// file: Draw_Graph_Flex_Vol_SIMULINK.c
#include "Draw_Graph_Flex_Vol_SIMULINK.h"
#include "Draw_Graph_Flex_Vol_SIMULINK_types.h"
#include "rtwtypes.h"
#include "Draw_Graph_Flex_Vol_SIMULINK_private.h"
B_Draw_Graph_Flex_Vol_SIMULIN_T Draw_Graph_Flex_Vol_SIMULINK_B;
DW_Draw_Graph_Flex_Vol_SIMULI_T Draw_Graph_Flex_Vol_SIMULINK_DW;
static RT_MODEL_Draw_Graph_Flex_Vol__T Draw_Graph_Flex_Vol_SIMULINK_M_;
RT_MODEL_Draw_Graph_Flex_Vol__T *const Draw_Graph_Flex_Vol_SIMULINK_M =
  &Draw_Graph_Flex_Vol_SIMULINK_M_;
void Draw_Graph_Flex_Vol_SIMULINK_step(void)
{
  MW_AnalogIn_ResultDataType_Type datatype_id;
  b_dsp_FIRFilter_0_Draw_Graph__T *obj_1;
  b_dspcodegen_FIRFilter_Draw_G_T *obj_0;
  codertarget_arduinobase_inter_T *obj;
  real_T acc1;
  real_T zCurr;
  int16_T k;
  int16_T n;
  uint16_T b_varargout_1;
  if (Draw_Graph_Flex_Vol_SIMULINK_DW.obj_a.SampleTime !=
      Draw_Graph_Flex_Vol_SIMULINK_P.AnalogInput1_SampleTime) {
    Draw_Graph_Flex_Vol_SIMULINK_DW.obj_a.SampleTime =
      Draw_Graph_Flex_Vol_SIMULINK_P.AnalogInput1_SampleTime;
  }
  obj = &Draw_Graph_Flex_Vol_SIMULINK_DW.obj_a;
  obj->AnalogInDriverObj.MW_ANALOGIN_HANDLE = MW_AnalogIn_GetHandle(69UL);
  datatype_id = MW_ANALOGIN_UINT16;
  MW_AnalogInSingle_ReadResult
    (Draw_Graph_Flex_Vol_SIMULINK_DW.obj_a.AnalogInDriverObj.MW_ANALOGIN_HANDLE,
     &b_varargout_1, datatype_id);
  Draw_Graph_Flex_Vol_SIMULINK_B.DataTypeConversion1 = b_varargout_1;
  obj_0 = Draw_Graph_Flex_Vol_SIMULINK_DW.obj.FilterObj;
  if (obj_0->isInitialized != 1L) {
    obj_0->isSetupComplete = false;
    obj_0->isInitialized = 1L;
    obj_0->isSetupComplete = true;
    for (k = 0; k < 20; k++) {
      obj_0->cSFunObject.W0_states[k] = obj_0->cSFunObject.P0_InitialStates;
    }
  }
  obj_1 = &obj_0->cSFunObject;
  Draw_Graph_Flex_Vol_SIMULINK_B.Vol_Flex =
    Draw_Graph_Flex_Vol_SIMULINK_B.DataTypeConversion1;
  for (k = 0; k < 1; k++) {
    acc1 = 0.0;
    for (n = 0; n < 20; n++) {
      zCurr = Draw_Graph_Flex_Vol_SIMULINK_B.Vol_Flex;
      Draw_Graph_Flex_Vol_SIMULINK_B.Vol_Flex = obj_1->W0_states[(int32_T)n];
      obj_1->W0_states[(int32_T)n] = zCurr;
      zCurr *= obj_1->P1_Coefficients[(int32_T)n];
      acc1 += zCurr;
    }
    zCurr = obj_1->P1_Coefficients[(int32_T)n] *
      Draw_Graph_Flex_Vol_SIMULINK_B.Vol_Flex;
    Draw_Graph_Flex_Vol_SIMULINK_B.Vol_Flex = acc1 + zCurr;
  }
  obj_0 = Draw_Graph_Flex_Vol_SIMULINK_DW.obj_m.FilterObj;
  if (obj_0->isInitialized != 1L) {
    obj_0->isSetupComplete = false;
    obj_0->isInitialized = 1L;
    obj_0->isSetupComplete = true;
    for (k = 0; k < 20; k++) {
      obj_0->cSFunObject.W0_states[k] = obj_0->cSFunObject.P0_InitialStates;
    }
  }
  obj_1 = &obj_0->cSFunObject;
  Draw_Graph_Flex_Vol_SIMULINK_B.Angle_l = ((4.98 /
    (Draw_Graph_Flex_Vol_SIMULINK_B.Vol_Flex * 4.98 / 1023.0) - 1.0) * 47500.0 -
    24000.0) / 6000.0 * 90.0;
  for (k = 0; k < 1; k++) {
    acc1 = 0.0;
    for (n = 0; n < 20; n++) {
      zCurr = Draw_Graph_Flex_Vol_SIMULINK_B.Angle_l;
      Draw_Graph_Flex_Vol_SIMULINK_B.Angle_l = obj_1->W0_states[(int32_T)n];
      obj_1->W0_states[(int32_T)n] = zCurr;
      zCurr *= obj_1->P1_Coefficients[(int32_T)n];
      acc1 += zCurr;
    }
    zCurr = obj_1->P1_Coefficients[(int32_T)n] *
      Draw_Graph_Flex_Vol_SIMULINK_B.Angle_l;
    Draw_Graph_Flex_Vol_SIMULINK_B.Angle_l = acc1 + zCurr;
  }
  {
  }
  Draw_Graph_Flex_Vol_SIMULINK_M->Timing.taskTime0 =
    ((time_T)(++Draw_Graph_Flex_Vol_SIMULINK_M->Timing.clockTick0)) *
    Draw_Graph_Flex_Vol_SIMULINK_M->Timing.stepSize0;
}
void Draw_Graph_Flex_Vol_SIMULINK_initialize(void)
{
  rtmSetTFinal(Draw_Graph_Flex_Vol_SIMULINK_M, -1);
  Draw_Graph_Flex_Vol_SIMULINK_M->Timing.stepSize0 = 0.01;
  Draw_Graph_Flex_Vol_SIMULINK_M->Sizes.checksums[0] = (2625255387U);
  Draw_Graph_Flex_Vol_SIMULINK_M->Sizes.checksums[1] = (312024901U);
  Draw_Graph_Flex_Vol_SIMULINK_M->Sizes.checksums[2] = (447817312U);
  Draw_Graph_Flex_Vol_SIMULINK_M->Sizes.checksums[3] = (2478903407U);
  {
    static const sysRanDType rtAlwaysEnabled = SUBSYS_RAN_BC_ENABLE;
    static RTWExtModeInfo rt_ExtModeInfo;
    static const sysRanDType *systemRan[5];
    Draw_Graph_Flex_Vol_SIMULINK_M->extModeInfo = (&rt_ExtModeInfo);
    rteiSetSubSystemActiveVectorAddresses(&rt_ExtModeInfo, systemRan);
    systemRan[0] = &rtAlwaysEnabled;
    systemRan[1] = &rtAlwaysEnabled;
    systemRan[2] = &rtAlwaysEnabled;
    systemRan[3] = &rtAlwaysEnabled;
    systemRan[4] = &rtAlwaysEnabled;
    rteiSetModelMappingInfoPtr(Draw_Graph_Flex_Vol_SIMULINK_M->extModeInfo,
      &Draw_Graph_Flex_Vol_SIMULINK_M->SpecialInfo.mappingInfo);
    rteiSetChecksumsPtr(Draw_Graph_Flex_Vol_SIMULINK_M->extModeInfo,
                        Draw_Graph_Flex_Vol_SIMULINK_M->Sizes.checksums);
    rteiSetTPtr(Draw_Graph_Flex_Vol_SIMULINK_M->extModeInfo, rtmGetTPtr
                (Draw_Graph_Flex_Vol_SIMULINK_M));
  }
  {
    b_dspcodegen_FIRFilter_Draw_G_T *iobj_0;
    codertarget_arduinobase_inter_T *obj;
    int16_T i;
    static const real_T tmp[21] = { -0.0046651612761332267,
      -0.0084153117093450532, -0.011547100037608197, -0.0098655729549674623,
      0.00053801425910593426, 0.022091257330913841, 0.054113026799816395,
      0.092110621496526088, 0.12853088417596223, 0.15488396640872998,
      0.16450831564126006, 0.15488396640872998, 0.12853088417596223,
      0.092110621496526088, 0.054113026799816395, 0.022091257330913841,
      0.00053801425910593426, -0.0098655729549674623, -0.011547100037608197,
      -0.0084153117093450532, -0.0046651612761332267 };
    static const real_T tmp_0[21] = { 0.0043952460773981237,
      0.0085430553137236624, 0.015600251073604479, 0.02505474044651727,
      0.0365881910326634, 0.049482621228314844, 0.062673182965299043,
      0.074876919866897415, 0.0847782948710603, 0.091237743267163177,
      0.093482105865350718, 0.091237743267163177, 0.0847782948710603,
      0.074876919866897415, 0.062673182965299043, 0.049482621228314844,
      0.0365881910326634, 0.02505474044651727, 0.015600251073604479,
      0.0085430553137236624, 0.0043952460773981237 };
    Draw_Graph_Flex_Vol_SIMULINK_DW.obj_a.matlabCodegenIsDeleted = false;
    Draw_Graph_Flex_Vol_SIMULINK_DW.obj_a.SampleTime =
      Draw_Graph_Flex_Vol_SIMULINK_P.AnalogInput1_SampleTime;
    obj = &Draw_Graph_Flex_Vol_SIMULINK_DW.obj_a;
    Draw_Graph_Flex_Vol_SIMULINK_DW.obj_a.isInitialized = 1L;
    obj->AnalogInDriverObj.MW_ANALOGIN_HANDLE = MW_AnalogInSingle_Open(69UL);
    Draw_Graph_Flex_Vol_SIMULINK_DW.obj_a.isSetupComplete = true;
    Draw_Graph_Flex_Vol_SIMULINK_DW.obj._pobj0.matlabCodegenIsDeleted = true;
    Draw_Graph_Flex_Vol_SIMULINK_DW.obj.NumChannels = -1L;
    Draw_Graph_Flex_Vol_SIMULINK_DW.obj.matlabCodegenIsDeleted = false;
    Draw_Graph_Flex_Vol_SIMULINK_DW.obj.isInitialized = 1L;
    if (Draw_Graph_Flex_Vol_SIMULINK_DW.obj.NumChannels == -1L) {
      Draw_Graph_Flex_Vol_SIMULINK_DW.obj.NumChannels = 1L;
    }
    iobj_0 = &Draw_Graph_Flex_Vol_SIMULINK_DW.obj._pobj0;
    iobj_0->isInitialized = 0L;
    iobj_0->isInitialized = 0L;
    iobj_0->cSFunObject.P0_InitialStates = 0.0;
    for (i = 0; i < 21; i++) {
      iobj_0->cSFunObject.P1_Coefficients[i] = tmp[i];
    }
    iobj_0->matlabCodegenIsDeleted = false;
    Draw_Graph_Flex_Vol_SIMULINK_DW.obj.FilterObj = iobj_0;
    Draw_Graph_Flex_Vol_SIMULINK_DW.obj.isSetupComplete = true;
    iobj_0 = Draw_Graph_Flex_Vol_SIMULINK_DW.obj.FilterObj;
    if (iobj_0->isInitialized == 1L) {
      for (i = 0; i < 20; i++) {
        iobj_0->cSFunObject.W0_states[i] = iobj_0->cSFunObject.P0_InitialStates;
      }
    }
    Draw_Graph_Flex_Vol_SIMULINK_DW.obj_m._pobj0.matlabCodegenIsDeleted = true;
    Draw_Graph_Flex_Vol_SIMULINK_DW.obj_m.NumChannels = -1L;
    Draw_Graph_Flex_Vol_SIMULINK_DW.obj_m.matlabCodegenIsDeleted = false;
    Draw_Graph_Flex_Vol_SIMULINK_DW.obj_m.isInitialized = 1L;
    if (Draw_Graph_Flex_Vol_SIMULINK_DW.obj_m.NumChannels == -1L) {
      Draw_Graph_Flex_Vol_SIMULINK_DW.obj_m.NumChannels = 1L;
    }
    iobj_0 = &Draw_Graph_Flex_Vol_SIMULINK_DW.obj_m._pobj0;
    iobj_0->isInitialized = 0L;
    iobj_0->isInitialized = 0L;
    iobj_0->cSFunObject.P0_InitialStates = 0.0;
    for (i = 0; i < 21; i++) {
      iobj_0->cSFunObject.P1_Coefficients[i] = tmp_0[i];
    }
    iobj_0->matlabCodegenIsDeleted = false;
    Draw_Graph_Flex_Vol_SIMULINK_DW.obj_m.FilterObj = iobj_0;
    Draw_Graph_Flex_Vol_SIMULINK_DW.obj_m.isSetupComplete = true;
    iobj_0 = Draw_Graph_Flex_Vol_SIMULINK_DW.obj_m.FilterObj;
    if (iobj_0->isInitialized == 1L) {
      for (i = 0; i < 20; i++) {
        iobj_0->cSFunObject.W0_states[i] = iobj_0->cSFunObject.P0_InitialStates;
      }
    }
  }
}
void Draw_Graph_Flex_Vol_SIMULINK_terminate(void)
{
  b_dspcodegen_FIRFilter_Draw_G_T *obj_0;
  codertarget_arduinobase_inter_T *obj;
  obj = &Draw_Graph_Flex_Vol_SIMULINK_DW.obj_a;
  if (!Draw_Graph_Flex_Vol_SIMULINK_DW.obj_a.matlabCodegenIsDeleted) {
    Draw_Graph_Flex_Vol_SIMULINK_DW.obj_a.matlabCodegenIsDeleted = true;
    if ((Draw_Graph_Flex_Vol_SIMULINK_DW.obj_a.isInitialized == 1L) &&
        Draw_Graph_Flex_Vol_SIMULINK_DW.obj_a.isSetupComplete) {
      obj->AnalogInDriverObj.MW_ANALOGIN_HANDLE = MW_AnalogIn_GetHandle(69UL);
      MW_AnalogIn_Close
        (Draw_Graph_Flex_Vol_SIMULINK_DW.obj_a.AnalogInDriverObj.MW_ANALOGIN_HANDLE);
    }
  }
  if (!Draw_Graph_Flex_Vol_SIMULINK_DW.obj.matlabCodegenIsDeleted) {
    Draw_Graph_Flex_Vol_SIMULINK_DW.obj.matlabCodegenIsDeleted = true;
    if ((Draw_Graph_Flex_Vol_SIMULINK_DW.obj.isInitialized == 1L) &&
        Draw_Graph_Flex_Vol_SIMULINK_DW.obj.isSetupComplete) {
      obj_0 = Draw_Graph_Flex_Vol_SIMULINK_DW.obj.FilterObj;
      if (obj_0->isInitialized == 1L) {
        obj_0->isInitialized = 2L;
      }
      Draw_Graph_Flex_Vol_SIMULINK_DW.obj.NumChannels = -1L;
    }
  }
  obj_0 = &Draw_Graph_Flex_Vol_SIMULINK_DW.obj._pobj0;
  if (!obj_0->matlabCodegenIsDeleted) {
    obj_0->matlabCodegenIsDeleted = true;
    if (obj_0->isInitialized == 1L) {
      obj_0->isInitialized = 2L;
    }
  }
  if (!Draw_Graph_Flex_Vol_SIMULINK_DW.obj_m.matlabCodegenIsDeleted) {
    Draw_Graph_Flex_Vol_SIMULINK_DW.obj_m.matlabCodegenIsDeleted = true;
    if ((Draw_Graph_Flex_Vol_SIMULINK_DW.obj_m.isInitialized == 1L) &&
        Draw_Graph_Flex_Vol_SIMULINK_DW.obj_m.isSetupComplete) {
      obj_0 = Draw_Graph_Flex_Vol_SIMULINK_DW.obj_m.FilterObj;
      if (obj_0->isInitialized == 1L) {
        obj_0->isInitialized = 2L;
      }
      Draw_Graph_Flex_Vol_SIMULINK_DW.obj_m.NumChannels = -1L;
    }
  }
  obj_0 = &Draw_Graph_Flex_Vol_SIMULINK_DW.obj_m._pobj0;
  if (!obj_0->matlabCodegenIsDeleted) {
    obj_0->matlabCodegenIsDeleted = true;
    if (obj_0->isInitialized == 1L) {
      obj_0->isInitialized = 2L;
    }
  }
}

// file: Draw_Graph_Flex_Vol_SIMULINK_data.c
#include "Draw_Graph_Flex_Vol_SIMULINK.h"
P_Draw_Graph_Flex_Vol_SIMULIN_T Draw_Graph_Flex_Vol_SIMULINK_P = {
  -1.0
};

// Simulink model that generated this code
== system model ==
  LowpassFilter#1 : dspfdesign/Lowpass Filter  <- 1: MATLABFunction#1
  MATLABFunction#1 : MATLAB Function  <- 1: LowpassFilter#2
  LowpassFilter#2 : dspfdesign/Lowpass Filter  <- 1: DataTypeConversion1
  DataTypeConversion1 : DataTypeConversion  <- 1: AnalogInput1
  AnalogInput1 : arduinolib/Analog Input  pinNumber=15
== matlab function MATLABFunction#1 ==
function Angle  = convert_flex_sensor(u)

VCC = 4.98;
R_DIV = 47500.0;
STRAIGHT_RESISTANCE = 24000.0;
BEND_RESISTANCE = 30000.0;

flexV = u * VCC / 1023.0;
flexR = R_DIV * (VCC / flexV - 1.0);

Angle = (((flexR - STRAIGHT_RESISTANCE)/(BEND_RESISTANCE - STRAIGHT_RESISTANCE))*90.0);
